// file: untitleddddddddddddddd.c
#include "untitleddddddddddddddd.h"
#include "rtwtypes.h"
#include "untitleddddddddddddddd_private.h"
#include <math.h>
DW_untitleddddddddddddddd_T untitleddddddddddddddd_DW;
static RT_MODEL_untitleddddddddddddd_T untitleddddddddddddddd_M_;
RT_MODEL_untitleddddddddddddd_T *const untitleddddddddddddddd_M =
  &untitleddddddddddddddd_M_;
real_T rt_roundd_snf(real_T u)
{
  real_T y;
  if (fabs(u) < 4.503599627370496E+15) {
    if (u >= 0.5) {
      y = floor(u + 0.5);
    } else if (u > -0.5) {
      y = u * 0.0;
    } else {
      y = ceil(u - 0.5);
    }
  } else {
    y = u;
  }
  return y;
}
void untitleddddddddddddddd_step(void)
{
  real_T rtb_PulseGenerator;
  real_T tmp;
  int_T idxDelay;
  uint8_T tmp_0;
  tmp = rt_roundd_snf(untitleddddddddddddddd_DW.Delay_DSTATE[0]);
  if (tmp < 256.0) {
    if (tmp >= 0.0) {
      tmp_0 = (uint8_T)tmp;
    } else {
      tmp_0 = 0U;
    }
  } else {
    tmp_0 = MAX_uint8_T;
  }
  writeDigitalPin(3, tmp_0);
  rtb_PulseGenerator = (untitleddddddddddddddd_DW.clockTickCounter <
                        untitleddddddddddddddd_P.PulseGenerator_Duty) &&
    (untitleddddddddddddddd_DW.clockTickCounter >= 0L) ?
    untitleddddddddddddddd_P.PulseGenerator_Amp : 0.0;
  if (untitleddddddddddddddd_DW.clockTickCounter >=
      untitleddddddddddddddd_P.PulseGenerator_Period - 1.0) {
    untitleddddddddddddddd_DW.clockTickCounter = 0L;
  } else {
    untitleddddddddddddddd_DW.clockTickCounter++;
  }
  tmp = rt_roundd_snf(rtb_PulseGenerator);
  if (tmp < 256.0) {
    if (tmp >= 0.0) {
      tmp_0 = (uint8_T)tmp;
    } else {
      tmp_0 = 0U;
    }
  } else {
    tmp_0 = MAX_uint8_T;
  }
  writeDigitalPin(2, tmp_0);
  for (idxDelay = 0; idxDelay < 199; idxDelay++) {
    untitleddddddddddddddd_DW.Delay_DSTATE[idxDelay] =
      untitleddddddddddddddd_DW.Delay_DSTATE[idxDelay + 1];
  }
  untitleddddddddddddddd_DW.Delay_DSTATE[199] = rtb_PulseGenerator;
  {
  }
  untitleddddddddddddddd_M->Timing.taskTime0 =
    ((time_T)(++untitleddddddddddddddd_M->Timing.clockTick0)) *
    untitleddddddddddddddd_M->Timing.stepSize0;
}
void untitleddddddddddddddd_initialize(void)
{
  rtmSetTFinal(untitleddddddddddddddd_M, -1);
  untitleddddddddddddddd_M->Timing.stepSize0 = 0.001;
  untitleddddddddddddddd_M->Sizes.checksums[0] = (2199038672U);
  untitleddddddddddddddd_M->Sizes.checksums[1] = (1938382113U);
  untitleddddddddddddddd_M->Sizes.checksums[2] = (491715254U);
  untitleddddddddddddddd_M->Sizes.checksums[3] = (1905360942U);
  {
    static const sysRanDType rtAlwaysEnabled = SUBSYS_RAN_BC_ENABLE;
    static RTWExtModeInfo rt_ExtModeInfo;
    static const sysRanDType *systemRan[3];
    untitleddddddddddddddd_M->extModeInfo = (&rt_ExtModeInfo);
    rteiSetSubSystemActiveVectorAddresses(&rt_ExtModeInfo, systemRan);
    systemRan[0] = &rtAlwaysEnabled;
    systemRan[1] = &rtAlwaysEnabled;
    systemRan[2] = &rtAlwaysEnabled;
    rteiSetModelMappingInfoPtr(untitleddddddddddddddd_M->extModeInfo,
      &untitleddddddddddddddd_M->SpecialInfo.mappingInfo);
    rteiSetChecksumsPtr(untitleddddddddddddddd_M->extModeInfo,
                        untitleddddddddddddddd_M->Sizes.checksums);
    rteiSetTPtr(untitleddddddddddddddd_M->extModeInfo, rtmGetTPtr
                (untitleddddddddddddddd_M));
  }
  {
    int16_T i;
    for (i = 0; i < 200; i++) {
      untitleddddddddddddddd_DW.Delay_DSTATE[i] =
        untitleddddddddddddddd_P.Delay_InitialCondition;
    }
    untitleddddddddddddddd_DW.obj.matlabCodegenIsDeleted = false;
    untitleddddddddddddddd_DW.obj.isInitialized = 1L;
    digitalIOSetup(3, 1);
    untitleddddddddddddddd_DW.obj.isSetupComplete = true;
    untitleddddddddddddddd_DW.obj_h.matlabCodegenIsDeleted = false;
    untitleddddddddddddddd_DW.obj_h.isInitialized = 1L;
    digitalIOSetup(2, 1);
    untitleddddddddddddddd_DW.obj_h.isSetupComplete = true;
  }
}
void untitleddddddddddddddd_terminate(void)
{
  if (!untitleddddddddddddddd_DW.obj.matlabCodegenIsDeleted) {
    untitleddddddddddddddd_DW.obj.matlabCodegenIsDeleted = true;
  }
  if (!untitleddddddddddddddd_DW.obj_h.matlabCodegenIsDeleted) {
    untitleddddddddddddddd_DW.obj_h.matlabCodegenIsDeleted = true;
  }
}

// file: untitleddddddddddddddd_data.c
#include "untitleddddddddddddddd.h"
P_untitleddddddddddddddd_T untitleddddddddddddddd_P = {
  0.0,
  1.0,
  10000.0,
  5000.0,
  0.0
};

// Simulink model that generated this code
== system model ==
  DigitalOutput#1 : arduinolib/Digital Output  pinNumber=3  <- 1: Delay
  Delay : Delay  DelayLength=200  <- 1: PulseGenerator
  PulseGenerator : DiscretePulseGenerator  Period=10  PulseWidth=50
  DigitalOutput#2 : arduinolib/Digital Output  pinNumber=2  <- 1: PulseGenerator
